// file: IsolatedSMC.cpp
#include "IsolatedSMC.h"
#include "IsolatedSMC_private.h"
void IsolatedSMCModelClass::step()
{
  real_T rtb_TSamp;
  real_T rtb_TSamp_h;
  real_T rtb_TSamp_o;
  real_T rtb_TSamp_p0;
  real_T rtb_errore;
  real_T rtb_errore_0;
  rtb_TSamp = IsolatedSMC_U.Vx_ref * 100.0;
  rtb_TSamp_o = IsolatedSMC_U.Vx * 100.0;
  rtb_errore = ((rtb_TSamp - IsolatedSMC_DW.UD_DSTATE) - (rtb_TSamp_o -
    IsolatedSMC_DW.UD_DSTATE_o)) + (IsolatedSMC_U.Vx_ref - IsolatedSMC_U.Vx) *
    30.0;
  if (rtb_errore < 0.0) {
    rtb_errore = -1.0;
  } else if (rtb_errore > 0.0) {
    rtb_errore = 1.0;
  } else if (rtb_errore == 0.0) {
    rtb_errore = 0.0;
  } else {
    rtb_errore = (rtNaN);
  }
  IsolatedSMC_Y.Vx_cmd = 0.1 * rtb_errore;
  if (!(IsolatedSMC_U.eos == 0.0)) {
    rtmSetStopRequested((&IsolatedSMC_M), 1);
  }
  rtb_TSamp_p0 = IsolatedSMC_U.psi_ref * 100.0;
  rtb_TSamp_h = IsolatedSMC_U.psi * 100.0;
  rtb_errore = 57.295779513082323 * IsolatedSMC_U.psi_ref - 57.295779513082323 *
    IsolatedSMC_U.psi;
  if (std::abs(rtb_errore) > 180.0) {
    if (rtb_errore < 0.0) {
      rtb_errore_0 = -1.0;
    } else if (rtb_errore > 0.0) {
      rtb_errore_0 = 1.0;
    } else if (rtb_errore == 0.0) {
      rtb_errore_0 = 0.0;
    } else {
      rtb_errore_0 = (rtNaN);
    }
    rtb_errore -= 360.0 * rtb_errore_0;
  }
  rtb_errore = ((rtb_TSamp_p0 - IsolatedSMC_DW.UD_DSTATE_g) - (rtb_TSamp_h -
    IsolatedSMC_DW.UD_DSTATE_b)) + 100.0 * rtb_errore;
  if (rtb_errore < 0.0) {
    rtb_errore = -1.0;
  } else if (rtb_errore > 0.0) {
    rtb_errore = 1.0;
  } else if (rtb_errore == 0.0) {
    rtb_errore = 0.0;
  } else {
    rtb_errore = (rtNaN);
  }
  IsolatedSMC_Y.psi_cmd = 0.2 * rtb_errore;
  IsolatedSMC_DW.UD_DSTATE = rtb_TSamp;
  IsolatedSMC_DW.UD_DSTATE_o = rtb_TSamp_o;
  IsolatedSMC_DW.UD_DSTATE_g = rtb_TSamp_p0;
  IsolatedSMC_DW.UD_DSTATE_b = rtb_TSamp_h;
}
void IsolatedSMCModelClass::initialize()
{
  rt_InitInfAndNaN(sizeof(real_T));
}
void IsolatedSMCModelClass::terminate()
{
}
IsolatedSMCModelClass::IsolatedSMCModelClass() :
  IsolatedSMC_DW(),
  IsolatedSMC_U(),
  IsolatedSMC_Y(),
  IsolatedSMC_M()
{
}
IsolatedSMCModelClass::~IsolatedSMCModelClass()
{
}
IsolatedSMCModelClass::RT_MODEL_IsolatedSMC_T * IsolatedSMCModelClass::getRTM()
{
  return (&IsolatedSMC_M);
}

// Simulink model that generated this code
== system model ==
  Vx_ref : Inport
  psi_ref : Inport
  psi : Inport
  Vx : Inport
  eos : Inport
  Vx_cmd : Outport  <- 1: MATLABFunction#1
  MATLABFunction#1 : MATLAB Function  <- 1: Sum#1, 2: Sum#2
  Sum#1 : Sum  Inputs=+-  <- 1: DiscreteDerivative#1, 2: DiscreteDerivative#2
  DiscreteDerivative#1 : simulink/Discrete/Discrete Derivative  gainval=1.0  <- 1: Vx_ref
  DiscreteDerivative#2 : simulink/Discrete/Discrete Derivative  gainval=1.0  <- 1: Vx
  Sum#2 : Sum  Inputs=+-  <- 1: Vx_ref, 2: Vx
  psi_cmd : Outport  <- 1: MATLABFunction#2
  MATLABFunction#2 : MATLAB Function  <- 1: Sum#3, 2: MATLABFunction#3
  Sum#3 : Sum  Inputs=+-  <- 1: DiscreteDerivative#3, 2: DiscreteDerivative#4
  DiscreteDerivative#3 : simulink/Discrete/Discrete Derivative  gainval=1.0  <- 1: psi_ref
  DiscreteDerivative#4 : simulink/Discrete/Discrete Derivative  gainval=1.0  <- 1: psi
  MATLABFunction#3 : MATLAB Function  <- 1: Gain#1, 2: Gain#2
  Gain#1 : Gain  Gain=180/pi  <- 1: psi_ref
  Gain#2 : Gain  Gain=180/pi  <- 1: psi
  Stop#1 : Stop  <- 1: CompareToZero#1
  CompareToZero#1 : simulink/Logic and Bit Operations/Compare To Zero  relop===  <- 1: CompareToZero#2
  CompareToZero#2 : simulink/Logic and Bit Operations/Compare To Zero  relop===  <- 1: eos
== matlab function MATLABFunction#1 ==
function Vx_cmd = SMC_Vx(Ax_err, Vx_err)
% SMC params
lamda = 30;
K = 0.1;
% Sliding surface
s = zeros(1);
s = (Ax_err) + lamda*(Vx_err);

Vx_cmd = K*sign(s);

== matlab function MATLABFunction#3 ==
function errore = fcn(psi_ref, psi_est)
errore=psi_ref-psi_est;

if abs(errore)>180
    errore=errore-360*sign(errore);
end

== matlab function MATLABFunction#2 ==
function psi_cmd = SMC_psi(psidot_error, psi_error)
% SMC params
lamda = 100;
K = 0.2;
% Sliding surface
s = zeros(1);
s = (psidot_error) + lamda*(psi_error);

psi_cmd = K*sign(s);
